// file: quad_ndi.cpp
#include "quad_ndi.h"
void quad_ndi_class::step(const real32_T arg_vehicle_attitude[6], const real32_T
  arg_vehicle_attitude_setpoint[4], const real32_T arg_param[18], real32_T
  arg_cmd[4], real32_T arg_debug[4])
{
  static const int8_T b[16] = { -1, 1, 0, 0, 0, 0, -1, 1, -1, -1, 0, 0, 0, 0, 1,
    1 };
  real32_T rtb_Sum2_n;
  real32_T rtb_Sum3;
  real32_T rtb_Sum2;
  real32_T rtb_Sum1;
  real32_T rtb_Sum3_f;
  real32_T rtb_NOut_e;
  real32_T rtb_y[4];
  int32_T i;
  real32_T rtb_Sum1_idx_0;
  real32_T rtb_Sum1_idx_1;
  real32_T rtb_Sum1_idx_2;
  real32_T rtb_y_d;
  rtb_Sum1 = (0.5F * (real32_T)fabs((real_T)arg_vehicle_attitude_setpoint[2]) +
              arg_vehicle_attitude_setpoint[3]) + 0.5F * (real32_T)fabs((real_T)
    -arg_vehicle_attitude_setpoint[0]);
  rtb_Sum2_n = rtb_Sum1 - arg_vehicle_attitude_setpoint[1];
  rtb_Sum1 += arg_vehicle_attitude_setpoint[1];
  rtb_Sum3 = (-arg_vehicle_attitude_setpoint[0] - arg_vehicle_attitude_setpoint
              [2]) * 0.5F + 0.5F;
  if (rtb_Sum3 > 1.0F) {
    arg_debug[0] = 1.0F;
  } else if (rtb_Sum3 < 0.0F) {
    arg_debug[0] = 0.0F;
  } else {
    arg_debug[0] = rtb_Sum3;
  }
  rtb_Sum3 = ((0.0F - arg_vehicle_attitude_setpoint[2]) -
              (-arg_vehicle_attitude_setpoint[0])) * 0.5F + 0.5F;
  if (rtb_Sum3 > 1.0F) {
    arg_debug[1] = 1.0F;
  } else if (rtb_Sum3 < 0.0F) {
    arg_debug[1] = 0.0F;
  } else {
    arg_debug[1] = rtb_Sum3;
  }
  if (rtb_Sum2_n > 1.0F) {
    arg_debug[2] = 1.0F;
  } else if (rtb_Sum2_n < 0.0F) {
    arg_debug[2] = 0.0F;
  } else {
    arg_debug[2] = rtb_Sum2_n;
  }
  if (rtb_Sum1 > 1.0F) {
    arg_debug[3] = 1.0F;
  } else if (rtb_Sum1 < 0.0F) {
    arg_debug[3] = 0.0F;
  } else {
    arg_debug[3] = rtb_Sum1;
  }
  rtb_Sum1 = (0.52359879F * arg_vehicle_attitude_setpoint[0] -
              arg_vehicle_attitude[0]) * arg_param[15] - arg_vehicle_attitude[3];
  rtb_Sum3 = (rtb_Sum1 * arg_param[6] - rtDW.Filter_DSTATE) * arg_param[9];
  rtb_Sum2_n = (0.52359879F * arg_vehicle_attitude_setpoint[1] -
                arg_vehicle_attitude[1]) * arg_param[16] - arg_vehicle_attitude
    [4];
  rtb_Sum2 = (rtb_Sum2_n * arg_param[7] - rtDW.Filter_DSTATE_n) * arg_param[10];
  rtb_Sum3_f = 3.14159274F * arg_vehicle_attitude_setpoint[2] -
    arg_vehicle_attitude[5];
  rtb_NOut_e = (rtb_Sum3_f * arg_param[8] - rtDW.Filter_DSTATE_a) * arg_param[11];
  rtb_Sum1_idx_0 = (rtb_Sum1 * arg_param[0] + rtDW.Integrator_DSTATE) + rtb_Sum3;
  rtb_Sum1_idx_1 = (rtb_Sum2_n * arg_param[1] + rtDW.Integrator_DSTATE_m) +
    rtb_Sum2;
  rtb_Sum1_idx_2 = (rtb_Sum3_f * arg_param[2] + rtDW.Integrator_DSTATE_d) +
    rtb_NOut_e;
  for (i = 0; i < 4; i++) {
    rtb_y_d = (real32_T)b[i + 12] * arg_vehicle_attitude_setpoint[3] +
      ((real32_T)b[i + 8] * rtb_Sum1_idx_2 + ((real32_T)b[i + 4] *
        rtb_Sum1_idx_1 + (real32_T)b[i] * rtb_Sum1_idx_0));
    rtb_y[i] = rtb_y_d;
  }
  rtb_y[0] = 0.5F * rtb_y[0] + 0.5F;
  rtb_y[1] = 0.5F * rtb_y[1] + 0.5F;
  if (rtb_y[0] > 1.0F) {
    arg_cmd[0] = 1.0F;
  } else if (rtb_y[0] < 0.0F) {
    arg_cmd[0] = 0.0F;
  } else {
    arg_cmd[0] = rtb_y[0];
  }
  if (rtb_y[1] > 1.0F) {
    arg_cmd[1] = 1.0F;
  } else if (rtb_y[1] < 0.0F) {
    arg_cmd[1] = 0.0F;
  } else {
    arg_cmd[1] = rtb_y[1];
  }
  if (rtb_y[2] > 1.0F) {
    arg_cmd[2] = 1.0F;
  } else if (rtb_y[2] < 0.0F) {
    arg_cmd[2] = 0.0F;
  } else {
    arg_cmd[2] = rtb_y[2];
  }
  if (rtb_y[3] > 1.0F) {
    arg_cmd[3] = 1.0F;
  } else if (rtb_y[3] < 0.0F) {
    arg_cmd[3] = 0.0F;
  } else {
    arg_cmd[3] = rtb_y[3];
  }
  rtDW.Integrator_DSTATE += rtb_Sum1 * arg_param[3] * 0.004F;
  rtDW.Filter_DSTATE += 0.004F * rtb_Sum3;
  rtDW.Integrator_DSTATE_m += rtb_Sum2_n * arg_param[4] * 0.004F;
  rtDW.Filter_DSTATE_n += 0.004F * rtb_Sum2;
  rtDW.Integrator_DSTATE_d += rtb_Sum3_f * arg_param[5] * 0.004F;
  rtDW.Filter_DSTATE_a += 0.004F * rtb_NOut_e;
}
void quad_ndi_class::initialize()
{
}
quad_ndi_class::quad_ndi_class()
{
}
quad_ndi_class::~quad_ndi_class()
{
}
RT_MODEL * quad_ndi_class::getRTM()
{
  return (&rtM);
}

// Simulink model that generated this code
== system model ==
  vehicle_attitude : Inport
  vehicle_attitude_setpoint : Inport
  param : Inport
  debug : Outport  <- 1: Saturate#1
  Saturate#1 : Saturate  UpperLimit=1  LowerLimit=0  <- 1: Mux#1
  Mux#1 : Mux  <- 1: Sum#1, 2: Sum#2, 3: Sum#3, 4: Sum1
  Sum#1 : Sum  Inputs=++  <- 1: Constant#1, 2: Gain#1
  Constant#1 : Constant  Value=0.5
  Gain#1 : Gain  Gain=0.5  <- 1: Sum3
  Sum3 : Sum  Inputs=+-  <- 1: Gain#2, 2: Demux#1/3
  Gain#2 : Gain  Gain=-1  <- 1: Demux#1
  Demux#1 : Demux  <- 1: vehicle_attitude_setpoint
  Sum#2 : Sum  Inputs=++  <- 1: Constant#1, 2: Gain#3
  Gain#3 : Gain  Gain=0.5  <- 1: Sum2
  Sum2 : Sum  Inputs=--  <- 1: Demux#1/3, 2: Gain#2
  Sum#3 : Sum  Inputs=-+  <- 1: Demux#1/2, 2: Sum#4
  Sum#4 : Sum  Inputs=+++  <- 1: Gain#4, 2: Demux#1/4, 3: Gain#5
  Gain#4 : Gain  Gain=0.5  <- 1: Abs#1
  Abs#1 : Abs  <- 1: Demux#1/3
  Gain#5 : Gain  Gain=0.5  <- 1: Abs#2
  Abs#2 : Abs  <- 1: Gain#2
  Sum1 : Sum  Inputs=++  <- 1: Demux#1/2, 2: Sum#4
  cmd : Outport  <- 1: Saturate#2
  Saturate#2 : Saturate  UpperLimit=1  LowerLimit=0  <- 1: MATLABFunction#1
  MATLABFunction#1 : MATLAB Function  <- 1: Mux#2
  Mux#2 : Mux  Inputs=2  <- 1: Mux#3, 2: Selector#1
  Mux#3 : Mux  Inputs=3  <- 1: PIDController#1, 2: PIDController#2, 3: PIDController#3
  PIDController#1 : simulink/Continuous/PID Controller  Controller=PID  TimeDomain=Discrete-time  IntegratorMethod=Forward Euler  Form=Parallel  P=1  I=1  D=1  N=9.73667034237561  InitialConditionForIntegrator=0  ExternalReset=none  LimitOutput=off  UpperSaturationLimit=inf  LowerSaturationLimit=-inf  <- 1: Sum#5, 2: Selector#2, 3: Selector#3, 4: Selector#4, 5: Selector#5
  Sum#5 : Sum  Inputs=+-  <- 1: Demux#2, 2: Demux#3
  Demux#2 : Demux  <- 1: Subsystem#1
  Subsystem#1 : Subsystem  <- 1: Selector#6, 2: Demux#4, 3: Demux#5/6
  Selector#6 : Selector  Indices=1:3  <- 1: vehicle_attitude_setpoint
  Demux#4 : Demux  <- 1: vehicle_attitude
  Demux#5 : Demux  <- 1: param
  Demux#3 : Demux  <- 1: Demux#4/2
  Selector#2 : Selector  Indices=1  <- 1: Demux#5
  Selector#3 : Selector  Indices=1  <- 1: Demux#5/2
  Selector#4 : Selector  Indices=1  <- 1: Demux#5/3
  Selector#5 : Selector  Indices=1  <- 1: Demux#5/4
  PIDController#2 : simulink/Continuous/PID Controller  Controller=PID  TimeDomain=Discrete-time  IntegratorMethod=Forward Euler  Form=Parallel  P=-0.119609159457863  I=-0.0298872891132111  D=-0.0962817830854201  N=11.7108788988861  InitialConditionForIntegrator=0  ExternalReset=none  LimitOutput=off  UpperSaturationLimit=inf  LowerSaturationLimit=-inf  <- 1: Sum#6, 2: Selector#7, 3: Selector#8, 4: Selector#9, 5: Selector#10
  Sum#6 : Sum  Inputs=-+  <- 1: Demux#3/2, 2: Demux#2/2
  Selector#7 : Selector  Indices=2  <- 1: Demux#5
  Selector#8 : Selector  Indices=2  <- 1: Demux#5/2
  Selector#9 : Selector  Indices=2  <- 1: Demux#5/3
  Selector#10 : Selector  Indices=2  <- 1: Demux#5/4
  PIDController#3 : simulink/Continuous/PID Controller  Controller=PID  TimeDomain=Discrete-time  IntegratorMethod=Forward Euler  Form=Parallel  P=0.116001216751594  I=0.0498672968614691  D=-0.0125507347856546  N=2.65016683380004  InitialConditionForIntegrator=0  ExternalReset=none  LimitOutput=off  UpperSaturationLimit=inf  LowerSaturationLimit=-inf  <- 1: Sum#7, 2: Selector#11, 3: Selector#12, 4: Selector#13, 5: Selector#14
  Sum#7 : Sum  Inputs=-+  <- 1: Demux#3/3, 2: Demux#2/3
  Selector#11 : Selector  Indices=3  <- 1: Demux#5
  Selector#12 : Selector  Indices=3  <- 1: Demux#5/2
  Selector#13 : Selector  Indices=3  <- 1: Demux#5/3
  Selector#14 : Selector  Indices=3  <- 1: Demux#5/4
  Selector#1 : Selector  Indices=4  <- 1: vehicle_attitude_setpoint
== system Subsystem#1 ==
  attitude_setpoint : Inport
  Inport#1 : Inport
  Inport#2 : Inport
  Outport#1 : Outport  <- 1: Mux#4
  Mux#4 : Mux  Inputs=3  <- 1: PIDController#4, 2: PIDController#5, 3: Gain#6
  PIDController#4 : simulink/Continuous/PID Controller  Controller=P  TimeDomain=Discrete-time  IntegratorMethod=Forward Euler  Form=Parallel  P=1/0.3  I=0  D=0  N=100  InitialConditionForIntegrator=0  ExternalReset=none  LimitOutput=off  UpperSaturationLimit=inf  LowerSaturationLimit=-inf  <- 1: Sum#8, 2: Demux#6
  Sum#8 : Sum  Inputs=+-  <- 1: Gain#7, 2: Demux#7
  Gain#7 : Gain  Gain=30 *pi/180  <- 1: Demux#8
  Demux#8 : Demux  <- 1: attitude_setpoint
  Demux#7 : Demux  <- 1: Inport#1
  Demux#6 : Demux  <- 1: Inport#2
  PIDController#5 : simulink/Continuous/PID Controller  Controller=P  TimeDomain=Discrete-time  IntegratorMethod=Forward Euler  Form=Parallel  P=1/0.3  I=0  D=0  N=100  InitialConditionForIntegrator=0  ExternalReset=none  LimitOutput=off  UpperSaturationLimit=inf  LowerSaturationLimit=-inf  <- 1: Sum#9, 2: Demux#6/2
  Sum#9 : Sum  Inputs=+-  <- 1: Gain#8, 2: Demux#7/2
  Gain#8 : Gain  Gain=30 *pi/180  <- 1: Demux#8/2
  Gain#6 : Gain  Gain=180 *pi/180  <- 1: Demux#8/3
== matlab function MATLABFunction#1 ==
function y = fcn(u)

% Mixing Matrix
%      R  P  Y  T
M =  [-1  0 -1  0;  % s1
       1  0 -1  0;  % s2
       0 -1  0  1;  % u1
       0  1  0  1]; % u2

% Mixing Matrix mit Steuergrößen multiplizieren   
y = (M * u);

% Servo Offset, da Servocommand 0 = 90° entspricht
y(1) = 0.5 + 0.5 * y(1);
y(2) = 0.5 + 0.5 * y(2);

y;
